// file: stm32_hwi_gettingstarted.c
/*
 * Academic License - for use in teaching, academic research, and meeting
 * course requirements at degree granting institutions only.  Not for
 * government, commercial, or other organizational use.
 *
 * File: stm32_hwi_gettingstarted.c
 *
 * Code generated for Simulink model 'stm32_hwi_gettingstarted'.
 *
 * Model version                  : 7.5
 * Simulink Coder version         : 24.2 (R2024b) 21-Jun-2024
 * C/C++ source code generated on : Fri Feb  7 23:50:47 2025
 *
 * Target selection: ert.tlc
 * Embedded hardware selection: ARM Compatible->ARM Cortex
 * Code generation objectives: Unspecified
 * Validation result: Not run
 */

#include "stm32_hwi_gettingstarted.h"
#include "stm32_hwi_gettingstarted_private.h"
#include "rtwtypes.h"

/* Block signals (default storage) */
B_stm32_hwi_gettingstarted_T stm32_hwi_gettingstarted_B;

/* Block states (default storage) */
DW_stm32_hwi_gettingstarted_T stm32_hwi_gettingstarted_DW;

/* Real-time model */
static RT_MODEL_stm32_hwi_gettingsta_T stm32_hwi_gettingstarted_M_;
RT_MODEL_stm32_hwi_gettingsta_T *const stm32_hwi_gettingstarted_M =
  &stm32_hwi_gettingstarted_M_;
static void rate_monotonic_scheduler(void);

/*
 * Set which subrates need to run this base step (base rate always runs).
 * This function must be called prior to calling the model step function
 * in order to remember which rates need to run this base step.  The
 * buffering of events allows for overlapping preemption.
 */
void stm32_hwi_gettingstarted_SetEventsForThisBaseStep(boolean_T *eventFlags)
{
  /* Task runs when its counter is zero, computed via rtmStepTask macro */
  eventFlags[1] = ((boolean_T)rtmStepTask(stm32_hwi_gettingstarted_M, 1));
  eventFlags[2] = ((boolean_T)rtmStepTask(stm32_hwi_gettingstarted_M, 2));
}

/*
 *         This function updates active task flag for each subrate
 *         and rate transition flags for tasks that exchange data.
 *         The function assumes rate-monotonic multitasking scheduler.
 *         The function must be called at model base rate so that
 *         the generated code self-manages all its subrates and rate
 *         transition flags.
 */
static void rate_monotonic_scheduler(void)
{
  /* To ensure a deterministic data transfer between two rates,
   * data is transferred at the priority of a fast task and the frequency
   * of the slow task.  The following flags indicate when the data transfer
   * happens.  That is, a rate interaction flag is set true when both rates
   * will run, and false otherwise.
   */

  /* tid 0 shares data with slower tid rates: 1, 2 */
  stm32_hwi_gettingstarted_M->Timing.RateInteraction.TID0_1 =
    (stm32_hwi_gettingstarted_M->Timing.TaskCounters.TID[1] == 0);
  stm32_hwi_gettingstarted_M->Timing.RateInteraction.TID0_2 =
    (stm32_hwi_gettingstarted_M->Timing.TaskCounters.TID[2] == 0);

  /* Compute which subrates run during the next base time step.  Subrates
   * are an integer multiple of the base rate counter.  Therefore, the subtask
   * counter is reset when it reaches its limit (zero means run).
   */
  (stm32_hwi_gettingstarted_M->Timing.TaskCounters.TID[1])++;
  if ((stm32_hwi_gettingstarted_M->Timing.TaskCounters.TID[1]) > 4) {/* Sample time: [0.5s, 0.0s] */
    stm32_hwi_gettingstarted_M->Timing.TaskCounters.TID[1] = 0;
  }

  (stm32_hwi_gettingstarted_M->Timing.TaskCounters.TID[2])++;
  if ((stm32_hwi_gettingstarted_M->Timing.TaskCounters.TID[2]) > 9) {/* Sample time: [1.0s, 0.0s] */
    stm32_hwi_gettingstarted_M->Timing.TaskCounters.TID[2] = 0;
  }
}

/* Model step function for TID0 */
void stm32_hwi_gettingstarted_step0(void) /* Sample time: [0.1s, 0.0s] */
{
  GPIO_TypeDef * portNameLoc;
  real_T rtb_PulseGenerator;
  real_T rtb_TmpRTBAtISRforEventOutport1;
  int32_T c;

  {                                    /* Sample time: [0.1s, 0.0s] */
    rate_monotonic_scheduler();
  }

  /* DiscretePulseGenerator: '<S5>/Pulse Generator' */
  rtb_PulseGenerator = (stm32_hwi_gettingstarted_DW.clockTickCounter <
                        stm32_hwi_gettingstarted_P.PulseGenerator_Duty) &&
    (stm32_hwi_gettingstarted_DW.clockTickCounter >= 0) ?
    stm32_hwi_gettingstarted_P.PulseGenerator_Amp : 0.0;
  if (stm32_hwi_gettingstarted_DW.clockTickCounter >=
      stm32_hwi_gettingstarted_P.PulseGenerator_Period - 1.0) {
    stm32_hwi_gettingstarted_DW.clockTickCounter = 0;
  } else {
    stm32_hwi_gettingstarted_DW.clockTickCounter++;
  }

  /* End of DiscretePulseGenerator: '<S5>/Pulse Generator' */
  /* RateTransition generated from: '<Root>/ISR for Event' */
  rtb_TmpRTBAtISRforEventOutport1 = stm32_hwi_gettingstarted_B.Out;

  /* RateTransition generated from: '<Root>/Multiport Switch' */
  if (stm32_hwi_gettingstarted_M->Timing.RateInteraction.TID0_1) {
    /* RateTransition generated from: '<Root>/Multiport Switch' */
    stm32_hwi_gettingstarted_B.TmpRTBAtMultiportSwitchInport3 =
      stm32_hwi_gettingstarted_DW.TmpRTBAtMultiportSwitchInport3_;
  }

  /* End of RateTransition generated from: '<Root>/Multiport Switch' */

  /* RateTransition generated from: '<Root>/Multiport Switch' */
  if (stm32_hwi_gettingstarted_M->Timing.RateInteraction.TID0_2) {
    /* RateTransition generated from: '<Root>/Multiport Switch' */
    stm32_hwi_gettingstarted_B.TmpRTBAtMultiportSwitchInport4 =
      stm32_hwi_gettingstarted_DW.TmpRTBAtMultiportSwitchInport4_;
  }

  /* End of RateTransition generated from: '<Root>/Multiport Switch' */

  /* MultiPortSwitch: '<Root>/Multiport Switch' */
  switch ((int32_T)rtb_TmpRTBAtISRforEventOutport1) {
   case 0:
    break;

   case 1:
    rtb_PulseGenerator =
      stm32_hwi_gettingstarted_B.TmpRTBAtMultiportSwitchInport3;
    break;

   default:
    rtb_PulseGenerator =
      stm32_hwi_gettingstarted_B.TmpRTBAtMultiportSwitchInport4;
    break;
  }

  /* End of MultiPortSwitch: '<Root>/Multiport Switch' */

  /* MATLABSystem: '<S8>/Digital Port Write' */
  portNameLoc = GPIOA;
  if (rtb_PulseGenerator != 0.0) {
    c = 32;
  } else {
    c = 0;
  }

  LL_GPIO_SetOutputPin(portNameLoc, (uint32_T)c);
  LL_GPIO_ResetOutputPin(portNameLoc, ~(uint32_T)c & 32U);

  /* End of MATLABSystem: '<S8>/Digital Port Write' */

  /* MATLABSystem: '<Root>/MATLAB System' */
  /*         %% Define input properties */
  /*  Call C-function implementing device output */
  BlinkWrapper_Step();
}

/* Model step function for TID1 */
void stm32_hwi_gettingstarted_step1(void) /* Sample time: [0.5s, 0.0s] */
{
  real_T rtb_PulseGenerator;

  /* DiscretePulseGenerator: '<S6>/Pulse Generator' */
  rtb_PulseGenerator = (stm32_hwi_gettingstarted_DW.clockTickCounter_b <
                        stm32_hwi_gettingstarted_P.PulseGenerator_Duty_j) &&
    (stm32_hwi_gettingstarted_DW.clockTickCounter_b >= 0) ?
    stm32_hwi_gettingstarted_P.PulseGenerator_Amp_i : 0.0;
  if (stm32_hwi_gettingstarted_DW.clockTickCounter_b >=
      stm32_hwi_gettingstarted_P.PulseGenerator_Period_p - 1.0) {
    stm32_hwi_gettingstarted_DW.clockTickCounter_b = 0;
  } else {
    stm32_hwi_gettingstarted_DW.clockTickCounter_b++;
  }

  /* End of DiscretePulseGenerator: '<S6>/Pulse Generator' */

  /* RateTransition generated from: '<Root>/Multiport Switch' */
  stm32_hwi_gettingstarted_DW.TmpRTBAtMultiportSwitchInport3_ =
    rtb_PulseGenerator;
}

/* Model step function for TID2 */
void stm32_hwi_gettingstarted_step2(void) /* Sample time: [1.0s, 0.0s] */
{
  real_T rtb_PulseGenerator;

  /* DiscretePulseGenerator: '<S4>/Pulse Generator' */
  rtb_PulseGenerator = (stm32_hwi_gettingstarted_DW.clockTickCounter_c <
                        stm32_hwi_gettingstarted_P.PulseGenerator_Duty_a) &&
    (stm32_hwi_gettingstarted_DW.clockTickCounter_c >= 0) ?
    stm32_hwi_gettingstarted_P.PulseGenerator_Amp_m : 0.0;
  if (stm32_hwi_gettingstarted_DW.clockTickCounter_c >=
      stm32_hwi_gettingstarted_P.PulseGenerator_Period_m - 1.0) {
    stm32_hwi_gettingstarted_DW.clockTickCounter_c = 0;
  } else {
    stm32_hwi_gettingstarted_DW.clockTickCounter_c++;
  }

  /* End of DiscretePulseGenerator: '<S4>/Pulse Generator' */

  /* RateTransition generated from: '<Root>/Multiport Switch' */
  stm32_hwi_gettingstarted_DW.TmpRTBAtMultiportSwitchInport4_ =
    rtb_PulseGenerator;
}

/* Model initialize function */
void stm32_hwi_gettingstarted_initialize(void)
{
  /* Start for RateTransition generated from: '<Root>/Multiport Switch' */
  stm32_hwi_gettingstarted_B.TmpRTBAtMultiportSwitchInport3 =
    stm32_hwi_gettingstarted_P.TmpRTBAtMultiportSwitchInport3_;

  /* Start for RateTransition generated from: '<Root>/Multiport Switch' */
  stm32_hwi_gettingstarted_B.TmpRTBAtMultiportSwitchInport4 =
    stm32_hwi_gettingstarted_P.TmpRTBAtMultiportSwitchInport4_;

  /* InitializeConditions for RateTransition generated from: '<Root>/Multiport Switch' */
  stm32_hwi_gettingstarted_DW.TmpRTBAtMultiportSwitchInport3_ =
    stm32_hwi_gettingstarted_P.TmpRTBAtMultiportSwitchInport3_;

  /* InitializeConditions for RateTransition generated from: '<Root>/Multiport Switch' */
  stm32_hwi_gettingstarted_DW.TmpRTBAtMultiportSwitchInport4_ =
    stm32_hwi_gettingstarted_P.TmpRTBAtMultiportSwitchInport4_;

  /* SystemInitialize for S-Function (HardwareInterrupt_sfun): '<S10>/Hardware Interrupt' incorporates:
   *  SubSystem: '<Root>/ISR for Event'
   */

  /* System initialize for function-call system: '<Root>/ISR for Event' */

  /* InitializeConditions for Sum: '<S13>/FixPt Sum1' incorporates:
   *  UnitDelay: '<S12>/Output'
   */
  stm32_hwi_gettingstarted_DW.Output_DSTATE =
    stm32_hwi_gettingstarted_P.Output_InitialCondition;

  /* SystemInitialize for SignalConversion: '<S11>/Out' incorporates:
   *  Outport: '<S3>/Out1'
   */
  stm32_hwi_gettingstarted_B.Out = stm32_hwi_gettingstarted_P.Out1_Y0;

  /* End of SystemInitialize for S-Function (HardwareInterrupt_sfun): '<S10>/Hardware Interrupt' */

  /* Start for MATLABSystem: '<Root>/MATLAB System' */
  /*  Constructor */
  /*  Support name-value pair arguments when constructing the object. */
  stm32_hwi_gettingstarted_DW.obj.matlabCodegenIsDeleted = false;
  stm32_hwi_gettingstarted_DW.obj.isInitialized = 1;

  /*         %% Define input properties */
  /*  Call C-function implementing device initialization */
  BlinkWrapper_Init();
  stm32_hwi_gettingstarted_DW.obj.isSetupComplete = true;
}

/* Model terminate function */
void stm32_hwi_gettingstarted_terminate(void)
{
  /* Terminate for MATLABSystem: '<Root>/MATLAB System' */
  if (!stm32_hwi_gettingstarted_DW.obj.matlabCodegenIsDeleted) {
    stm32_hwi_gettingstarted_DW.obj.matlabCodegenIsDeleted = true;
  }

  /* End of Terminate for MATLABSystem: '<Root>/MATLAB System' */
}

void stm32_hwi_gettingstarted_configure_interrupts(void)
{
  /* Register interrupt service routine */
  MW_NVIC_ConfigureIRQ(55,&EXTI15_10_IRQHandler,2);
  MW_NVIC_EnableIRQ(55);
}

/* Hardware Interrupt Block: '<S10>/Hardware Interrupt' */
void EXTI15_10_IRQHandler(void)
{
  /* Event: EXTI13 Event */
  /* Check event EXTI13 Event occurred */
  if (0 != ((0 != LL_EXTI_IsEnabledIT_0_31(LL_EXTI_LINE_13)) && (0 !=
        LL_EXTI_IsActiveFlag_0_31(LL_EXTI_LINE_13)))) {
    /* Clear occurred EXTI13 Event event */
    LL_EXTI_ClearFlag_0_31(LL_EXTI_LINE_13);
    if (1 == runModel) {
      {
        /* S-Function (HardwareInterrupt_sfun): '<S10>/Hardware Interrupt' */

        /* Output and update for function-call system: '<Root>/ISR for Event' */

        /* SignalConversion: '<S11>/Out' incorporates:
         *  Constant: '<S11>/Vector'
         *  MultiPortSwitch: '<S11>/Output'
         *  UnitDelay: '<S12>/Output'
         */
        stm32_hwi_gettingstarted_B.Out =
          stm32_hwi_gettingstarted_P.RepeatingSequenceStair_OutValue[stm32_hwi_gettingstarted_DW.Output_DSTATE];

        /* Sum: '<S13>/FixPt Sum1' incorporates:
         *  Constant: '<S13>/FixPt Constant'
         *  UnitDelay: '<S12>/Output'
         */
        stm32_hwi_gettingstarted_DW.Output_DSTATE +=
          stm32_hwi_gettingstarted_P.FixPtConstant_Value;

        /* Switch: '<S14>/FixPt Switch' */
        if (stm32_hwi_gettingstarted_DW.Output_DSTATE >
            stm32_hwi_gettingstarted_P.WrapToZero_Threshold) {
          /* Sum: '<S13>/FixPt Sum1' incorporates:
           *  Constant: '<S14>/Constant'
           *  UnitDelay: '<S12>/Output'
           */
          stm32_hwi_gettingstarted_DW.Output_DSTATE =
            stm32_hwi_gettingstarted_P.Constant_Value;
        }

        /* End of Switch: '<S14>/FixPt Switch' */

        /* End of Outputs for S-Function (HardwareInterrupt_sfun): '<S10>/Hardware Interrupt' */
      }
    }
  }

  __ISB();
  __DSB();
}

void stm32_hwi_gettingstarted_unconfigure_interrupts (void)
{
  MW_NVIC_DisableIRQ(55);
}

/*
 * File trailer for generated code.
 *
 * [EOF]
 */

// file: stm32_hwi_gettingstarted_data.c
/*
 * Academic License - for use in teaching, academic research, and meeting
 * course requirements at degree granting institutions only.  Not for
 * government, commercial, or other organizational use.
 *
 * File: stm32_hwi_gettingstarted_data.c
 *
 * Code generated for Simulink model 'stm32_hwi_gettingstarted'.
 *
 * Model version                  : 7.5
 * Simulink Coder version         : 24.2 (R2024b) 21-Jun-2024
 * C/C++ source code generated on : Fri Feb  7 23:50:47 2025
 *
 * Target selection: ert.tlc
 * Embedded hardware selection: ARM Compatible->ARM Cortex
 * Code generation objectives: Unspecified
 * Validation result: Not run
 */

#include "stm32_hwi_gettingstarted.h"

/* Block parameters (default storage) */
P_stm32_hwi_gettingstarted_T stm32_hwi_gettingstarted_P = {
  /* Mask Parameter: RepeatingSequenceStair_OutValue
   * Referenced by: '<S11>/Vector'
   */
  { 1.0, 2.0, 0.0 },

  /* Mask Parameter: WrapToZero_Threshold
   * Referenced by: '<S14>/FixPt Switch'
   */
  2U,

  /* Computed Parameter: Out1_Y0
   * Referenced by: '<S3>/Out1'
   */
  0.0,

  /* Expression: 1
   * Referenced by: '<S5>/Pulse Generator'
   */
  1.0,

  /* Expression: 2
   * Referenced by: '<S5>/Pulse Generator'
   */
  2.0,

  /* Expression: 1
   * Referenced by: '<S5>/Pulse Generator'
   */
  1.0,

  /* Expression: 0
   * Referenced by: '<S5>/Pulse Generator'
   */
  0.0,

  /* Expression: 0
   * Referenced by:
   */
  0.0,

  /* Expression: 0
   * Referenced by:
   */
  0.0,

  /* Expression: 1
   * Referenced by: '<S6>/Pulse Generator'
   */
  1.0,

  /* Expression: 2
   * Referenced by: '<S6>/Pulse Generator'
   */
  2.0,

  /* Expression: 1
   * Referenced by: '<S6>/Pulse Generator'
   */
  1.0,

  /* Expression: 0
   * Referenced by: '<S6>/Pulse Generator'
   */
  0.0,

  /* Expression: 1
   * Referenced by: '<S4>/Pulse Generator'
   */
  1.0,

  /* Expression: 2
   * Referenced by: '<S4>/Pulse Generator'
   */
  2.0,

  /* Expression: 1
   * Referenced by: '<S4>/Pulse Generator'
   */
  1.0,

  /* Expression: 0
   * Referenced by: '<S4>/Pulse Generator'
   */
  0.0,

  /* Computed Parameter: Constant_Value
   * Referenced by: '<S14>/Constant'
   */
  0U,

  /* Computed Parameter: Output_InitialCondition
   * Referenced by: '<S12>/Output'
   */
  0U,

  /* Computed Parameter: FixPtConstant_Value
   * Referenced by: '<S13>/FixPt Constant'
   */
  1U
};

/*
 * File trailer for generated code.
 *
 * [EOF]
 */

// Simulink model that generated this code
simulink model "stm32_hwi_gettingstarted"  (R2024b)
settings: Solver=FixedStepAuto  StartTime=0.0  StopTime=inf  RelTol=1e-3  EnableMultiTasking=on
libraries: stm32f4xxblockslib x2, simulink x1

== system stm32_hwi_gettingstarted ==
  note: Getting Started with Hardware Interrupt block for
      | STMicroelectronics STM32F4xx Based Hardware Board
  note: Copyright 2021 The MathWorks, Inc.
  Blue LED : stm32f4xxblockslib/Digital Port Write  PortName=GPIOA  PinNumber=5  ReadOperation=off  IOAsArray=off  EnableSimPort=off  hoistedMaskSrc=ECSoC/ECSimCodegen/Digital Port Write
  Hardware Interrupt1 : stm32f4xxblockslib/Hardware Interrupt  ISRGroup=External interrupts (EXTI)  ISRName=EXTI15_10_IRQHandler  ISRNumber=55  EventsList={ 'off', 'EXTI15 Event', '1'; 'off', 'EXTI14 Event', '2'; 'on', 'EXTI13 Event', '3'; 'off', 'EXTI12 Event', '4'; 'off', 'EXTI11 Event', '5'; 'off', 'EXTI10 Event', '6'; 'off', 'Custom event', '7' }  SelectedEvents={'EXTI13 Event'}  TaskPriority=30  DisablePreemption=off  ClearInterruptFlagsAtEndOfEvent=off  InterruptDefinitionFile=$(TARGET_ROOT)/registry/interrupts/STM32F4xxBased_interrupts.xml  HardwareBoard=STM32F4xx Based  EnableSimPort=off
  ISR for Event : Subsystem  TreatAsAtomicUnit=on
  MATLAB System : MATLABSystem  System=Sink
  Multiport Switch : MultiPortSwitch  DataPortOrder=Zero-based contiguous  zeroidx=on  SaturateOnIntegerOverflow=off  InputSameDT=off
  Toggle at every 1000ms : Subsystem
  Toggle at every 100ms : Subsystem
  Toggle at every 500ms : Subsystem
  wires:
  Toggle at every 500ms/1(Out1) -> Multiport Switch/3
  Toggle at every 1000ms/1(Out1) -> Multiport Switch/4
  ISR for Event/1(Out1) -> Multiport Switch/1
  Toggle at every 100ms/1(Out1) -> Multiport Switch/2
  Hardware Interrupt1/1 -> ISR for Event/Trigger
  Multiport Switch/1 -> Blue LED/1

== system stm32_hwi_gettingstarted/ISR for Event ==
  function : TriggerPort  TriggerType=function-call  VariantControl=(inherit)
  Repeating Sequence Stair : simulink/Sources/Repeating Sequence Stair  OutValues=[1 2 0]  tsamp=-1  OutMin=[]  OutMax=[]  OutDataTypeStr=double  OutputDataTypeScalingMode=double  OutDataType=fixdt(0,8)  ConRadixGroup=Best Precision: Vector-wise  OutScaling=2^-12
  Out1 : Outport
  wires:
  Repeating Sequence Stair/1 -> Out1/1

== system stm32_hwi_gettingstarted/Toggle at every 1000ms ==
  Pulse Generator : DiscretePulseGenerator
  Out1 : Outport
  wires:
  Pulse Generator/1 -> Out1/1

== system stm32_hwi_gettingstarted/Toggle at every 100ms ==
  Pulse Generator : DiscretePulseGenerator  SampleTime=0.1
  Out1 : Outport
  wires:
  Pulse Generator/1 -> Out1/1

== system stm32_hwi_gettingstarted/Toggle at every 500ms ==
  Pulse Generator : DiscretePulseGenerator  SampleTime=0.5
  Out1 : Outport
  wires:
  Pulse Generator/1 -> Out1/1
